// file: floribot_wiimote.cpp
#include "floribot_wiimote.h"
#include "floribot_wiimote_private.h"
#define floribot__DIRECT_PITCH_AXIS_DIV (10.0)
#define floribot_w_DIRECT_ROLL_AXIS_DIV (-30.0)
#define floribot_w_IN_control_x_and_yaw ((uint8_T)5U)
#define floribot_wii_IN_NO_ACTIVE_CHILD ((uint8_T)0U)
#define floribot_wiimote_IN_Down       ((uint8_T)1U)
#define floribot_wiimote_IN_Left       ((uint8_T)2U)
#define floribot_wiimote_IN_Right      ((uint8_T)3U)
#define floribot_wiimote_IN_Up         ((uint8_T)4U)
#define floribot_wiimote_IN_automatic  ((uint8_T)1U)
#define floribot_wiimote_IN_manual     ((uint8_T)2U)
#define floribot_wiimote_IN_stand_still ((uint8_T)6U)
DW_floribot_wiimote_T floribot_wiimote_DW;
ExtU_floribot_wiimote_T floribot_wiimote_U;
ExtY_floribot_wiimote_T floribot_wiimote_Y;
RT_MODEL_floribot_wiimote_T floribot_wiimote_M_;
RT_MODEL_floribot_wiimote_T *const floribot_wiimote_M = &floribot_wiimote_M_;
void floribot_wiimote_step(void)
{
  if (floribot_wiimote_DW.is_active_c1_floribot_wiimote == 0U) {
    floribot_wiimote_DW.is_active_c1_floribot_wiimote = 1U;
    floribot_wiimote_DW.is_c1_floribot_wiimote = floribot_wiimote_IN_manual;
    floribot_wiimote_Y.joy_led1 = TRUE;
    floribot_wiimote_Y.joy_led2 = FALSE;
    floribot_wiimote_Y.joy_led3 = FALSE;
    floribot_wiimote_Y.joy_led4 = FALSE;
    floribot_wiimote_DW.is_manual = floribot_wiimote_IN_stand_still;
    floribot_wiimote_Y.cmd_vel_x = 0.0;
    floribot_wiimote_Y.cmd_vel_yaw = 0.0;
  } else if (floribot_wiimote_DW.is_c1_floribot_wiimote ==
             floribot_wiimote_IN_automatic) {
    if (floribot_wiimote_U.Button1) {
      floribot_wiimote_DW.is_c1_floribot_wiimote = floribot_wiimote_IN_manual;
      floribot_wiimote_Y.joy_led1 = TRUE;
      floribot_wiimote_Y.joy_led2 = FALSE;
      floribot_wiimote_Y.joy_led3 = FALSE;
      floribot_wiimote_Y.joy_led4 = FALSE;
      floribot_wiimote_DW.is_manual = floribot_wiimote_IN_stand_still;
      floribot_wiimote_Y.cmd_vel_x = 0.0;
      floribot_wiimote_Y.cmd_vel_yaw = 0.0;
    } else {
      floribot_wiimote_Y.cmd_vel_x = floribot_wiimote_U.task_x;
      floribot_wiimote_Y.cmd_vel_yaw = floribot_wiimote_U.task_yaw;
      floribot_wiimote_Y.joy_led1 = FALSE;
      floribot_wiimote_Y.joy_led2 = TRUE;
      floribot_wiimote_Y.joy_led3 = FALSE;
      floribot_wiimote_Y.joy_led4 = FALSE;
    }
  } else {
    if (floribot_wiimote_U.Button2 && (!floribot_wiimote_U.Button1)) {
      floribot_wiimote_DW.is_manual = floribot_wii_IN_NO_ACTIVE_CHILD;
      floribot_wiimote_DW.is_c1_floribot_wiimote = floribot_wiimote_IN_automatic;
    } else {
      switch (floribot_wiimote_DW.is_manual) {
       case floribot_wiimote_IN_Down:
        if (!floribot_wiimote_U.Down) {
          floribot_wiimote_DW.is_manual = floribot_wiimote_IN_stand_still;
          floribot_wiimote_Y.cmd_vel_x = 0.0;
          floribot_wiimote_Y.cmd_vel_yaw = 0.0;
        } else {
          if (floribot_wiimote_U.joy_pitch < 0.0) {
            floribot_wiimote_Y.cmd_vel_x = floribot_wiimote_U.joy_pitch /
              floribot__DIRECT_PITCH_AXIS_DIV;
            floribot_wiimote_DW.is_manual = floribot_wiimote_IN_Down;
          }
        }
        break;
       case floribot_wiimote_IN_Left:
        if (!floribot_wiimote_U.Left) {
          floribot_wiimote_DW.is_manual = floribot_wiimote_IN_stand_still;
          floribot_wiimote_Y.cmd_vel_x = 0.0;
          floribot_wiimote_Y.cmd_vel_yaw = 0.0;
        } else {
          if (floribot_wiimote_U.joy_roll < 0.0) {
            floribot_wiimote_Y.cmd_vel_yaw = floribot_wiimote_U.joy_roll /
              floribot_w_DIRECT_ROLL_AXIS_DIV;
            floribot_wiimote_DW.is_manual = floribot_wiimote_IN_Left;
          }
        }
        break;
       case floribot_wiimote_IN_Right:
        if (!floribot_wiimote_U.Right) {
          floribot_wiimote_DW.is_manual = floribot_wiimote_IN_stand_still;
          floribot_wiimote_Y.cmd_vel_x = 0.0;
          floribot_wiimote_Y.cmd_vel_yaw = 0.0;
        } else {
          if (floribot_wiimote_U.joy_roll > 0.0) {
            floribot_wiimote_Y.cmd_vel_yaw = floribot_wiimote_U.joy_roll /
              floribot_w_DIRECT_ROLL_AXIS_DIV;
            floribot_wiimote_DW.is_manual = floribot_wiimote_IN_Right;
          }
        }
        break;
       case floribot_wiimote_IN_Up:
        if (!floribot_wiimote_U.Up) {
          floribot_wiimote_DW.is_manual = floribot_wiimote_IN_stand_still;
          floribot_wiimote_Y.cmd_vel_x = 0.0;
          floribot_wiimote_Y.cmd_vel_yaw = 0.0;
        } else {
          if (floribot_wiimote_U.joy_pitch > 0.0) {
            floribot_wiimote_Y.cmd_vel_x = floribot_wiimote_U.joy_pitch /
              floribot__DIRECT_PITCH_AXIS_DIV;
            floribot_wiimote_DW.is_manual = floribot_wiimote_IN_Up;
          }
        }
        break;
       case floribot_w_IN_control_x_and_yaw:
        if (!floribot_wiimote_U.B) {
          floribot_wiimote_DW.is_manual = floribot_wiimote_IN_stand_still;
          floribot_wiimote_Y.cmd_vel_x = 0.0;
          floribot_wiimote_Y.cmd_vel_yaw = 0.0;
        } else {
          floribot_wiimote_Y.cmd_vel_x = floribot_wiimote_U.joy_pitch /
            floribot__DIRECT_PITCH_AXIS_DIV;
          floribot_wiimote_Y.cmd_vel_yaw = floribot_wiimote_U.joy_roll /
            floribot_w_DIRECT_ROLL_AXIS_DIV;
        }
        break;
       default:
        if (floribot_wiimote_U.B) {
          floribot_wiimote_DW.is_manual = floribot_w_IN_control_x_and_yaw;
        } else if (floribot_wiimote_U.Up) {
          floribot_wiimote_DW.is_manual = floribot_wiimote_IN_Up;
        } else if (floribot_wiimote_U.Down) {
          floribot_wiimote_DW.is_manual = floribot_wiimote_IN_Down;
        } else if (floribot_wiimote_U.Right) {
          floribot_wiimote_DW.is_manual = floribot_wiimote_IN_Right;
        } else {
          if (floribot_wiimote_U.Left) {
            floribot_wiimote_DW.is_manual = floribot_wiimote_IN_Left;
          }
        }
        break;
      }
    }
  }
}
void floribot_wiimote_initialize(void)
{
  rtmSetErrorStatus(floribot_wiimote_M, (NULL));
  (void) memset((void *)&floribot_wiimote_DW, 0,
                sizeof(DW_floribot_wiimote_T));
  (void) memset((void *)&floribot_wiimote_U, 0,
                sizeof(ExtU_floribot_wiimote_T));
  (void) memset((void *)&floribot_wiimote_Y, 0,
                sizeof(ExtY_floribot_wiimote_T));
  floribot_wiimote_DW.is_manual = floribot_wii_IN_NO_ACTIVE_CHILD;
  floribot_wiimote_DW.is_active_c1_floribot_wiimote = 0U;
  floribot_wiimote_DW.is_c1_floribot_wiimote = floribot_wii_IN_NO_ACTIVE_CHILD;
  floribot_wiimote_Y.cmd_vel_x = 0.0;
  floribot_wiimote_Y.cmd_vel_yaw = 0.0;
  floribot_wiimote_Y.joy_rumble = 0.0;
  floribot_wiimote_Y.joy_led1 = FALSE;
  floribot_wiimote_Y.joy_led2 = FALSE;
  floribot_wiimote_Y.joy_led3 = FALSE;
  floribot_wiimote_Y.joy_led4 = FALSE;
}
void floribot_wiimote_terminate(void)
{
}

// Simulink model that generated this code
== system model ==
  Inport#1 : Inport
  Inport#2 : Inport
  Button1 : Inport
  Button2 : Inport
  joy_pitch : Inport
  joy_roll : Inport
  Inport#3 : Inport
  task_x : Inport
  task_yaw : Inport
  Up : Inport
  Down : Inport
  Right : Inport
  Left : Inport
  cmd_vel_x : Outport  <- 1: Stateflowchart#1
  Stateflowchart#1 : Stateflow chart  <- 1: Inport#1, 2: Inport#2, 3: Button1, 4: Button2, 5: Up, 6: Down, 7: Right, 8: Left, 9: joy_pitch, 10: joy_roll, 11: Inport#3, 12: task_x, 13: task_yaw
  cmd_vel_yaw : Outport  <- 1: Stateflowchart#1/2
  joy_rumble : Outport  <- 1: Stateflowchart#1/3
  joy_led1 : Outport  <- 1: Stateflowchart#1/4
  joy_led2 : Outport  <- 1: Stateflowchart#1/5
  joy_led3 : Outport  <- 1: Stateflowchart#1/6
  joy_led4 : Outport  <- 1: Stateflowchart#1/7
== stateflow chart Stateflowchart#1 ==
  state manual
    joy_led1 = true;
    joy_led2 = false;
    joy_led3 = false;
    joy_led4 = false;
    state stand_still
      cmd_vel_x = 0;
      cmd_vel_yaw = 0;
    state control_x_and_yaw
      during:
      cmd_vel_x = joy_pitch/DIRECT_PITCH_AXIS_DIV;
      cmd_vel_yaw = joy_roll/DIRECT_ROLL_AXIS_DIV;
    state Up
    state Down
    state Right
    state Left
    (default) -> stand_still
    stand_still -> control_x_and_yaw [order 1] : [B]
    control_x_and_yaw -> stand_still : [!B]
    Up -> Up [order 2] : [joy_pitch > 0]/cmd_vel_x = joy_pitch/DIRECT_PITCH_AXIS_DIV;
    stand_still -> Up [order 2] : [Up]
    Up -> stand_still [order 1] : [!Up]
    stand_still -> Down [order 3] : [Down]
    Down -> Down [order 2] : [joy_pitch < 0]/cmd_vel_x = joy_pitch/DIRECT_PITCH_AXIS_DIV;
    Down -> stand_still [order 1] : [!Down]
    stand_still -> Right [order 4] : [Right]
    Right -> Right [order 2] : [joy_roll > 0]/cmd_vel_yaw = joy_roll/DIRECT_ROLL_AXIS_DIV;
    Right -> stand_still [order 1] : [!Right]
    Left -> Left [order 2] : [joy_roll < 0]/cmd_vel_yaw = joy_roll/DIRECT_ROLL_AXIS_DIV;
    stand_still -> Left [order 5] : [Left]
    Left -> stand_still [order 1] : [!Left]
  state automatic
    during:
    cmd_vel_x = task_x;
    cmd_vel_yaw = task_yaw;
    joy_led1 = false;
    joy_led2 = true;
    joy_led3 = false;
    joy_led4 = false;
  (default) -> manual
  automatic -> manual : [Button1]
  manual -> automatic : [Button2 && !Button1]
  data: A input boolean; B input boolean; Button1 input boolean; Button2 input boolean; Up input boolean; Down input boolean; Right input boolean; Left input boolean; joy_pitch input double; joy_roll input double; joy_yaw input double; task_x input double; task_yaw input double; cmd_vel_x output double; cmd_vel_yaw output double; joy_rumble output double; joy_led1 output boolean; joy_led2 output boolean; joy_led3 output boolean; joy_led4 output boolean; DIRECT_PITCH_AXIS_DIV constant double =10; DIRECT_ROLL_AXIS_DIV constant double =-30
